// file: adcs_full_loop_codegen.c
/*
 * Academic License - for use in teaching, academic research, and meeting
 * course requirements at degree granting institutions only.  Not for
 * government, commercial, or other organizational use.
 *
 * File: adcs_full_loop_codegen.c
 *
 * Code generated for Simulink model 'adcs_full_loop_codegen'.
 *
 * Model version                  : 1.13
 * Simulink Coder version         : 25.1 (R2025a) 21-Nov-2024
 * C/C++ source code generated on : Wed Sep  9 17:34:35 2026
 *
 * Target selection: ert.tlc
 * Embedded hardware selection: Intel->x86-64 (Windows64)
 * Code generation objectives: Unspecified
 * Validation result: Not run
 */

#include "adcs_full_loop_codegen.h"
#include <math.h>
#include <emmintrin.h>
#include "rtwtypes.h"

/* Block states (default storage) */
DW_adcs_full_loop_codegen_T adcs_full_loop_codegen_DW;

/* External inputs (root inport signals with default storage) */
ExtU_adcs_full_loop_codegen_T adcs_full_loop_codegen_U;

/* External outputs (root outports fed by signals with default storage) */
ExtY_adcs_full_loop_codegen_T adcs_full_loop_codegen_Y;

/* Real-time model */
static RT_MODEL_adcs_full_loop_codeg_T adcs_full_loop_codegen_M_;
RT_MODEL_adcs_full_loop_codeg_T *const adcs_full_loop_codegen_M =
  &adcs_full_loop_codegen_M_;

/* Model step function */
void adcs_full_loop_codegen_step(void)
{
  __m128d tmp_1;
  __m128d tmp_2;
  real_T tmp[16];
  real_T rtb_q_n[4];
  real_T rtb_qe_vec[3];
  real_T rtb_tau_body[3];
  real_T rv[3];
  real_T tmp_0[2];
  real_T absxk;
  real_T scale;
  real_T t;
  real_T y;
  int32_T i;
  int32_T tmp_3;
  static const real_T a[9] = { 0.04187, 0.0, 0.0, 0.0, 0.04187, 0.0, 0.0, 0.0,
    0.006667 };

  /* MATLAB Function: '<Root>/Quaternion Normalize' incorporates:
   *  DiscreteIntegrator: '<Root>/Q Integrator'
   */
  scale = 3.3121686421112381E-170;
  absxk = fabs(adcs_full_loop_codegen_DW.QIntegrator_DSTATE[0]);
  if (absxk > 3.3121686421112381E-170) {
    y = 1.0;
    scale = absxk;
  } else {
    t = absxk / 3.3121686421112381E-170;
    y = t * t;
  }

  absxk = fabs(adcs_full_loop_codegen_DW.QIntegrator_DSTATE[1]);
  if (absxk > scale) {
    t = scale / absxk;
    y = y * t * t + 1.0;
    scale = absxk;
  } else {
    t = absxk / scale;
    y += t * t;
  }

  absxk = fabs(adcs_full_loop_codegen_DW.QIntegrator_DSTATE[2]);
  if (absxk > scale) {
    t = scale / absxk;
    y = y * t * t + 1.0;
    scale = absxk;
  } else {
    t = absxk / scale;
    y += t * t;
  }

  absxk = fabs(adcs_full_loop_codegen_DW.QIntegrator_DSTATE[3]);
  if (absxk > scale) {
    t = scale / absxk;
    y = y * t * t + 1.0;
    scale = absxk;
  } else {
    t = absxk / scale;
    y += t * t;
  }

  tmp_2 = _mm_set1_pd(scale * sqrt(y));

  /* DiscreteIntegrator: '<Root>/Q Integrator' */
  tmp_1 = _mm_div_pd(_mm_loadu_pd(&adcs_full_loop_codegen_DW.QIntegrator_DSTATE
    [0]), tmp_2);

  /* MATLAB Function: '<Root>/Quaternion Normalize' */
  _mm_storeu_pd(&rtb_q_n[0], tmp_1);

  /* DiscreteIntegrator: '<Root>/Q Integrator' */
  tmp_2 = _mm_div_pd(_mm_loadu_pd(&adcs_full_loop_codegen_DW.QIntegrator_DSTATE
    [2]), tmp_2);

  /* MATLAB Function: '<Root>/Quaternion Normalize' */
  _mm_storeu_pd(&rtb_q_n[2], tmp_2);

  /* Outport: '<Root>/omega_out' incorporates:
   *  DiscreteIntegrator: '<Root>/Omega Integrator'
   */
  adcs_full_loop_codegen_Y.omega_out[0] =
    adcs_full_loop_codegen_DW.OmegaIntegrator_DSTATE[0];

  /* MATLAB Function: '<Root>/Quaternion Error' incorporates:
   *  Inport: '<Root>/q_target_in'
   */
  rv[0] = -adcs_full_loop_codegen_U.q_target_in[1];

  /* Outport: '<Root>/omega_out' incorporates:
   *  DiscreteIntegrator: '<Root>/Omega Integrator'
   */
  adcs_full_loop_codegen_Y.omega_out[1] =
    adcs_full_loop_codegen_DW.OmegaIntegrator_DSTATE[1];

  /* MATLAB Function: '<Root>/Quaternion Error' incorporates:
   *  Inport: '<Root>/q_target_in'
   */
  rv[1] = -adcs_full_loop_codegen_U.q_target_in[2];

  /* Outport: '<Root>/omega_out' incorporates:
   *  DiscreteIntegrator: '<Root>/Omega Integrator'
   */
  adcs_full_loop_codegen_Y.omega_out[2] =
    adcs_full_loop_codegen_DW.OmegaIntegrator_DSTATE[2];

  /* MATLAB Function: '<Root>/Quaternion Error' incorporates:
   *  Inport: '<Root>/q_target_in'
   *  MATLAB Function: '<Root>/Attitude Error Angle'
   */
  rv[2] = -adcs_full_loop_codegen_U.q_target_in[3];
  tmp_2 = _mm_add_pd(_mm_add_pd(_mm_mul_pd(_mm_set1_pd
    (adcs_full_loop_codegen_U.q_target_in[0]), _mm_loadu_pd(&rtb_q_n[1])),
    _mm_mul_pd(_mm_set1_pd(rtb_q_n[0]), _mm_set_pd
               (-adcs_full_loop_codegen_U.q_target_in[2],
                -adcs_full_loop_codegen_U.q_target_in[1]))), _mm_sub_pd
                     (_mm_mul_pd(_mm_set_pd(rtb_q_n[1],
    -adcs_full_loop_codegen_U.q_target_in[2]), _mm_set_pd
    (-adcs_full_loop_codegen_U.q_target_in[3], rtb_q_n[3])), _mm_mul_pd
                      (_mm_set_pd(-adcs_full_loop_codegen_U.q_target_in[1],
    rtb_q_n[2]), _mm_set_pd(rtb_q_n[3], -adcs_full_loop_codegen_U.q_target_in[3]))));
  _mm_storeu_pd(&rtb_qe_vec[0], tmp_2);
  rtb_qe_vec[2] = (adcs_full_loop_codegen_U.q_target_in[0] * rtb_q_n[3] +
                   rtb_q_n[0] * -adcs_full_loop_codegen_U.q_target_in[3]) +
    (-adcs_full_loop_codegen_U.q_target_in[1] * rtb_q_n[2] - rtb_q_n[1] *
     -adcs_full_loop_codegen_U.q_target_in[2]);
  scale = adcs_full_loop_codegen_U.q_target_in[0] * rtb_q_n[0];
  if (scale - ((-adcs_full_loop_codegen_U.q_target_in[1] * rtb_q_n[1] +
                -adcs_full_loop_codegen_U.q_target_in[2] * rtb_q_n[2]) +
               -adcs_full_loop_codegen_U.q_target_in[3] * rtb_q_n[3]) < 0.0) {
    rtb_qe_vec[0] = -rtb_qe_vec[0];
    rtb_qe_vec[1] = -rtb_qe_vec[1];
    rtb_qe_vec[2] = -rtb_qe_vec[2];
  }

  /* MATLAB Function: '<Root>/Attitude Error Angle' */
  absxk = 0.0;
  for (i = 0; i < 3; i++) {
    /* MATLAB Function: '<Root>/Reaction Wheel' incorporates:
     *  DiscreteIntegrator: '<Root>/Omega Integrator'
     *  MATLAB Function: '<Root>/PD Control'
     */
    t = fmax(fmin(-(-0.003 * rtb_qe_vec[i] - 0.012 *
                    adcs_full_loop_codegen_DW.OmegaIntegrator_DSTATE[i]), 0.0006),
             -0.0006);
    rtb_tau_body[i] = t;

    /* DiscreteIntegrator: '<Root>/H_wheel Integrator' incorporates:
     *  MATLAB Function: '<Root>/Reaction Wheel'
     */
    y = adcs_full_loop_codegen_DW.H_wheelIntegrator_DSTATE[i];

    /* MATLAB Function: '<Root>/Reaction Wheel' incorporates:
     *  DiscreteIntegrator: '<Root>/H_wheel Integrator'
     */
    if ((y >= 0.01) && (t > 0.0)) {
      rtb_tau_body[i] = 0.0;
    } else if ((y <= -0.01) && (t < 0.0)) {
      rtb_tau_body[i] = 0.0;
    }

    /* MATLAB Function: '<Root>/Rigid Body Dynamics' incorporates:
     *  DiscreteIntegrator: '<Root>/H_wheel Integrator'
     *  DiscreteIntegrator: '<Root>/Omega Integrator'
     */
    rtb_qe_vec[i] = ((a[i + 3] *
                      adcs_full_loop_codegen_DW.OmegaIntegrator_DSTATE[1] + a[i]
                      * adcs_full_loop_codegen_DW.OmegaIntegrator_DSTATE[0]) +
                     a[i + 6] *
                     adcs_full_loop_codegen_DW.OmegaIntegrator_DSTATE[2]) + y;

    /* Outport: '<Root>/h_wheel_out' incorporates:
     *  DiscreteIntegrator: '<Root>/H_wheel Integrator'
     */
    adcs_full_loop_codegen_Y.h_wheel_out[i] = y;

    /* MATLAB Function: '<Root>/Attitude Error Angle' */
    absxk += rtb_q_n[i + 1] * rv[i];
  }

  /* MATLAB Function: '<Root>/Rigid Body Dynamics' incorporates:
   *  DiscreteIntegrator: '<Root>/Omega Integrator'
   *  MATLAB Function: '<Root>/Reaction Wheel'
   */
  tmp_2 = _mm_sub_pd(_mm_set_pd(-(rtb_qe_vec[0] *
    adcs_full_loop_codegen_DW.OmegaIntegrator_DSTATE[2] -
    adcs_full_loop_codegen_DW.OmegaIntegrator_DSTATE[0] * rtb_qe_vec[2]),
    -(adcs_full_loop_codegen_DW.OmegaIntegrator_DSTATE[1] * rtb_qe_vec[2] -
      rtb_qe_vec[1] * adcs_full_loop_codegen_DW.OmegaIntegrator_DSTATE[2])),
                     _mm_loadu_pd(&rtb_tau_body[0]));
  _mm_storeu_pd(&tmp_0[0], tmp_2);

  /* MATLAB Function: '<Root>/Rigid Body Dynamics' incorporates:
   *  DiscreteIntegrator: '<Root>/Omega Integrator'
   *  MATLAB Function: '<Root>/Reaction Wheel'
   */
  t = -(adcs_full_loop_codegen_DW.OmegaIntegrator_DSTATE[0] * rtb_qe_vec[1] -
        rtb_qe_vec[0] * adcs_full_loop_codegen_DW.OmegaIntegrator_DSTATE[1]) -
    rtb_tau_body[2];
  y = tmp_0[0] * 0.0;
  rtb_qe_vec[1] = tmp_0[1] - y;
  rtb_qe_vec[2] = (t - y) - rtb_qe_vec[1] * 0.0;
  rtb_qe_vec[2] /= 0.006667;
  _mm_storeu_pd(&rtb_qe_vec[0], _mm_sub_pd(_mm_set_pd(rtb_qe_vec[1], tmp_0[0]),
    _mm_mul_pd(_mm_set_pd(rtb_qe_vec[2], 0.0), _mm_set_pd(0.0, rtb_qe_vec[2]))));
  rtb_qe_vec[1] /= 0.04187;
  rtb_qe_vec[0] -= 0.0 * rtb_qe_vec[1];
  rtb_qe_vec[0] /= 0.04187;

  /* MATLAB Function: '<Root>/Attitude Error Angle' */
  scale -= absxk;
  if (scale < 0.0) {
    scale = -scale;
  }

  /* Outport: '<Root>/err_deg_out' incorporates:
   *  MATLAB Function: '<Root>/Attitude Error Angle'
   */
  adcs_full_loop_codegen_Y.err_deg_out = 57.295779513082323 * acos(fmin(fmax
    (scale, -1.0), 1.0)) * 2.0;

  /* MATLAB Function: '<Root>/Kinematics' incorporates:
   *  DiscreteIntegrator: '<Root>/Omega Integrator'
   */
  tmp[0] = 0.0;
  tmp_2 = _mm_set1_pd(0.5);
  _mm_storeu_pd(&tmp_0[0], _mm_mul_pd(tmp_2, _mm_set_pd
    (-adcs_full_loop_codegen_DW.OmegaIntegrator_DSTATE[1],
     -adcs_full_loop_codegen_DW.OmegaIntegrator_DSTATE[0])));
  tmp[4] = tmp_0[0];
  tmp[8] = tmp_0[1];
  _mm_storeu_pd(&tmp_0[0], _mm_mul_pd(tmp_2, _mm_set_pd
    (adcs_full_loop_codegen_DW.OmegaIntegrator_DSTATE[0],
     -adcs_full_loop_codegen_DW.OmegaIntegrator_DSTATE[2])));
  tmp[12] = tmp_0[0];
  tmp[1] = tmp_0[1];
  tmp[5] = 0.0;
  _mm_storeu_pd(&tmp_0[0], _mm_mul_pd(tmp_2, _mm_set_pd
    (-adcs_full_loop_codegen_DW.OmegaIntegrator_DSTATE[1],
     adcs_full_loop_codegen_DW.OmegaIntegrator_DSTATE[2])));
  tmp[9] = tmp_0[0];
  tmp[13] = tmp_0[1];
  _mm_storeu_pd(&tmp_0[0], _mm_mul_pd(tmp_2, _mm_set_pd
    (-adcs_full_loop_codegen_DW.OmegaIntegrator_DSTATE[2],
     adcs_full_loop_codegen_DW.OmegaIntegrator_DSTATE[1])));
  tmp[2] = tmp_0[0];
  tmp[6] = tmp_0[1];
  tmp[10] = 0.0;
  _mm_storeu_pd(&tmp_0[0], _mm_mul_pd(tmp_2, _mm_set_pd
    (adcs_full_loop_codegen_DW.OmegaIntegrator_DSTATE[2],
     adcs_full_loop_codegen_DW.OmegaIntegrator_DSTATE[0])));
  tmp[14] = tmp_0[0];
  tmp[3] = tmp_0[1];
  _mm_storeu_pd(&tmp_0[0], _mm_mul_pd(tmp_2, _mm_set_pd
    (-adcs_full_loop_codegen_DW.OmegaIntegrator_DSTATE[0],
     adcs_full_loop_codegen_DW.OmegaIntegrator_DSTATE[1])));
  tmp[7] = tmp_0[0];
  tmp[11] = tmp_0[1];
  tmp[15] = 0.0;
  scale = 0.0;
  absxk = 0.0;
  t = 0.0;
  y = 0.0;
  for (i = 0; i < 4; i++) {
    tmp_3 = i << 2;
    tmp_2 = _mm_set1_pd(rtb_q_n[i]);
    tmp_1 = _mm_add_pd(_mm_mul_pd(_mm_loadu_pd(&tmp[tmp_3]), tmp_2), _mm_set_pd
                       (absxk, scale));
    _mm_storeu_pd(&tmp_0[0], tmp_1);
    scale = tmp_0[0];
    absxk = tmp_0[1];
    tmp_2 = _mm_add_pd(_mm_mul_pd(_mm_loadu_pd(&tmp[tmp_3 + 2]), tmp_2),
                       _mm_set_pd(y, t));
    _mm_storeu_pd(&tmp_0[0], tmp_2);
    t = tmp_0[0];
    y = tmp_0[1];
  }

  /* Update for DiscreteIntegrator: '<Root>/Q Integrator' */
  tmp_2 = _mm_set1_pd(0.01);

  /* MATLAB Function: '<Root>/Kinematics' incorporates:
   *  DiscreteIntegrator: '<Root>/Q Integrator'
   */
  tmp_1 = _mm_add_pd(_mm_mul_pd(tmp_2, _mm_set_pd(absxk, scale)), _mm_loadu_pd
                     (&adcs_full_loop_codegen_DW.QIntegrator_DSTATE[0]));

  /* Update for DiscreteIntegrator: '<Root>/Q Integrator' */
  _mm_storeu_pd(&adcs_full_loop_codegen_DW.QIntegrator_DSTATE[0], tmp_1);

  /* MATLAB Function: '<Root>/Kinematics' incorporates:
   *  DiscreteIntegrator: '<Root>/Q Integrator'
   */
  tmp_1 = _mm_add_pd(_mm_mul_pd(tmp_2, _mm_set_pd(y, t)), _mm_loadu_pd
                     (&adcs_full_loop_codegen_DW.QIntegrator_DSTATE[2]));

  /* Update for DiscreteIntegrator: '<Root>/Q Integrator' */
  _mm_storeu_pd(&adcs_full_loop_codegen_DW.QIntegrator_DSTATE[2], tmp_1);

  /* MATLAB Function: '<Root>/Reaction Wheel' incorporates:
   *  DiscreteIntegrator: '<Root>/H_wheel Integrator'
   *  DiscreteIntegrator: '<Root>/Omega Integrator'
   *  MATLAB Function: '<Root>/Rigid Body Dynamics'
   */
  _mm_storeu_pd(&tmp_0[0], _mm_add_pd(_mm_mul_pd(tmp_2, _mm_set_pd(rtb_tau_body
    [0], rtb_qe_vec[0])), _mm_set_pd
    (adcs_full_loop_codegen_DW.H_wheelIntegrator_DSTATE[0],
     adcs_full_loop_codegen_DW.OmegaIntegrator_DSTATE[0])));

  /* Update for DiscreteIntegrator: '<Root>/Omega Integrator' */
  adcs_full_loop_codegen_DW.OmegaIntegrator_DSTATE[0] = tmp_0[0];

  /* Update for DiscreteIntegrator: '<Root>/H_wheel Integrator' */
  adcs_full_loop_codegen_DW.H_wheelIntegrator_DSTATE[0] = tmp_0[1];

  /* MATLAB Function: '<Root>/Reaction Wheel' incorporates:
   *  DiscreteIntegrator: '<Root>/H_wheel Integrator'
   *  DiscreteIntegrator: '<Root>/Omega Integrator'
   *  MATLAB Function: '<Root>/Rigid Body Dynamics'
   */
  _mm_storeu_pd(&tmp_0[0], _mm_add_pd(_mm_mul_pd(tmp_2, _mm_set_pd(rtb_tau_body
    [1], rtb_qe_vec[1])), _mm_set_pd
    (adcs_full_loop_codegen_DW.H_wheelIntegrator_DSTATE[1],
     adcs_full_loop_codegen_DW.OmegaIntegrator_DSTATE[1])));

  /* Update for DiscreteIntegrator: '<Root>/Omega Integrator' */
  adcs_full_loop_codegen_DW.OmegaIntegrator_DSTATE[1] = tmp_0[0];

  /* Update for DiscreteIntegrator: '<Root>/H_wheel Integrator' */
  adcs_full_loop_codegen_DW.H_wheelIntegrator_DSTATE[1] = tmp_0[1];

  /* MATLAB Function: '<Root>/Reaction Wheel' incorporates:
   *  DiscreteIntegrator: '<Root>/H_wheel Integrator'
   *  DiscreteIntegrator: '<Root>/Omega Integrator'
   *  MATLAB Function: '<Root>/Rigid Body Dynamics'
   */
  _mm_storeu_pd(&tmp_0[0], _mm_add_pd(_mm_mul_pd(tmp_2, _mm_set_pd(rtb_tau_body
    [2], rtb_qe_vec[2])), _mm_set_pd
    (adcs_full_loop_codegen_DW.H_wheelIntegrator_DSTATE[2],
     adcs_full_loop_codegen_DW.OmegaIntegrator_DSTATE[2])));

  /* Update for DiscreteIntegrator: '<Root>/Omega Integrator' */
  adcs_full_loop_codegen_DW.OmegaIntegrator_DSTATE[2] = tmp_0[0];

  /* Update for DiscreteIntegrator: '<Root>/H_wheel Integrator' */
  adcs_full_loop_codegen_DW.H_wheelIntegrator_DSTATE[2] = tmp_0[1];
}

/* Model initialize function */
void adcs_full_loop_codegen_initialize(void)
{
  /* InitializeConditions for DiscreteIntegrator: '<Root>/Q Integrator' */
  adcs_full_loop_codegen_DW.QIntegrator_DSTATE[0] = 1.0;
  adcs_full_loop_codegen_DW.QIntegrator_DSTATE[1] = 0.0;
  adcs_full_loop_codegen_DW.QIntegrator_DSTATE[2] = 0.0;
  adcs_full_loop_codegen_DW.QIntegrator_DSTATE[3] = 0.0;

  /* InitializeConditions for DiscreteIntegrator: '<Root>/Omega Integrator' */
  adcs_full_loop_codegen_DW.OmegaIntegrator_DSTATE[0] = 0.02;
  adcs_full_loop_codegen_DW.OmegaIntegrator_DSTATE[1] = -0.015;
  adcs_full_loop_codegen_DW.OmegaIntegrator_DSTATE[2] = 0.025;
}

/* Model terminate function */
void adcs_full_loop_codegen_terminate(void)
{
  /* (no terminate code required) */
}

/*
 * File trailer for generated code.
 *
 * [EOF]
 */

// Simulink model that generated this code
simulink model "adcs_full_loop_codegen"  (R2025a)
settings: Solver=ode4  StartTime=0.0  StopTime=800  FixedStep=0.01  RelTol=1e-8
undefined symbols (not defined in the file): DiscIntNeverNeededParam

== system adcs_full_loop_codegen ==
  q_target_in : Inport  PortDimensions=4
  Attitude Error Angle : MATLAB Function  TreatAsAtomicUnit=on
  Display : Display
  Display1 : Display
  Display2 : Display
  Error Scope : Scope
  H_wheel Integrator : DiscreteIntegrator  InitialCondition=[0;0;0]  SampleTime=0.01  ICPrevOutput=DiscIntNeverNeededParam  ICPrevScaledInput=DiscIntNeverNeededParam
  H_wheel Scope : Scope
  Kinematics : MATLAB Function  TreatAsAtomicUnit=on
  Omega Integrator : DiscreteIntegrator  InitialCondition=[0.02;-0.015;0.025]  SampleTime=0.01  ICPrevOutput=DiscIntNeverNeededParam  ICPrevScaledInput=DiscIntNeverNeededParam
  Omega Scope : Scope
  PD Control : MATLAB Function  TreatAsAtomicUnit=on
  Q Integrator : DiscreteIntegrator  InitialCondition=[1;0;0;0]  SampleTime=0.01  ICPrevOutput=DiscIntNeverNeededParam  ICPrevScaledInput=DiscIntNeverNeededParam
  Quaternion Error : MATLAB Function  TreatAsAtomicUnit=on
  Quaternion Normalize : MATLAB Function  TreatAsAtomicUnit=on
  Reaction Wheel : MATLAB Function  TreatAsAtomicUnit=on
  Rigid Body Dynamics : MATLAB Function  TreatAsAtomicUnit=on
  err_deg_out : Outport
  omega_out : Outport  Port=2
  h_wheel_out : Outport  Port=3
  wires:
  q_target_in/1 -> Attitude Error Angle/1(q_target), Quaternion Error/1(q_target)
  Quaternion Normalize/1(q_n) -> Attitude Error Angle/2(q), Quaternion Error/2(q), Kinematics/1(q)
  Q Integrator/1 -> Quaternion Normalize/1(q)
  Attitude Error Angle/1(err_deg) -> Error Scope/1, Display/1, err_deg_out/1
  PD Control/1(tau_cmd) -> Reaction Wheel/1(tau_cmd_body)
  Quaternion Error/1(qe_vec) -> PD Control/1(qe_vec)
  H_wheel Integrator/1 -> Reaction Wheel/2(h_wheel), Rigid Body Dynamics/2(h_wheel), h_wheel_out/1, H_wheel Scope/1, Display1/1
  Reaction Wheel/2(h_wheel_dot) -> H_wheel Integrator/1, Rigid Body Dynamics/3(h_wheel_dot)
  Omega Integrator/1 -> PD Control/2(omega), omega_out/1, Kinematics/2(omega), Rigid Body Dynamics/1(omega), Omega Scope/1, Display2/1
  Rigid Body Dynamics/1(omega_dot) -> Omega Integrator/1
  Kinematics/1(q_dot) -> Q Integrator/1

== matlab function adcs_full_loop_codegen/Kinematics ==
function q_dot = kinematics_block(q, omega)
    wx = omega(1); wy = omega(2); wz = omega(3);
    Omega = [ 0 -wx -wy -wz; wx 0 wz -wy; wy -wz 0 wx; wz wy -wx 0 ];
    q_dot = 0.5 * Omega * q;
end

== matlab function adcs_full_loop_codegen/Reaction Wheel ==
function [tau_body, h_wheel_dot] = reaction_wheel_block(tau_cmd_body, h_wheel)
    h_max = 0.01; tau_max = 0.0006;   % same values as reaction_wheel_model.m
    tau_wheel_cmd = -tau_cmd_body;     % same sign fix as the debugged .m version
    tau_actual = zeros(3,1);
    for i = 1:3
        tau_actual(i) = max(min(tau_wheel_cmd(i), tau_max), -tau_max);
    end
    for i = 1:3
        if (h_wheel(i) >= h_max && tau_actual(i) > 0) || ...
           (h_wheel(i) <= -h_max && tau_actual(i) < 0)
            tau_actual(i) = 0;
        end
    end
    h_wheel_dot = tau_actual;
    tau_body = -tau_actual;
end

== matlab function adcs_full_loop_codegen/Quaternion Normalize ==
function q_n = normalize_block(q)
    q_n = q / norm(q);
end

== matlab function adcs_full_loop_codegen/Attitude Error Angle ==
function err_deg = error_angle_block(q_target, q)
    q0 = q(1); qv = q(2:4);
    r0 = q_target(1); rv = -q_target(2:4);
    qe0 = r0*q0 - dot(rv,qv);
    if qe0 < 0, qe0 = -qe0; end
    qe0 = min(max(qe0,-1),1);
    err_deg = 2*acosd(qe0);
end

== matlab function adcs_full_loop_codegen/Quaternion Error ==
function qe_vec = quaternion_error_block(q_target, q)
    q0 = q(1); qv = q(2:4);
    r0 = q_target(1); rv = -q_target(2:4);  % conjugate of q_target inline
    qe0 = r0*q0 - dot(rv,qv);
    qe_vec = r0*qv + q0*rv + cross(rv,qv);
    if qe0 < 0
        qe_vec = -qe_vec;   % shortest-path correction, same as pid_attitude_control.m
    end
end

== matlab function adcs_full_loop_codegen/PD Control ==
function tau_cmd = pd_control_block(qe_vec, omega)
    Kp = 3e-3;   % SAME gains as main_pointing.m -- keep in sync if you retune
    Kd = 1.2e-2;
    tau_cmd = -Kp*qe_vec - Kd*omega;
end

== matlab function adcs_full_loop_codegen/Rigid Body Dynamics ==
function omega_dot = rigid_body_dynamics_block(omega, h_wheel, h_wheel_dot)
    I = diag([0.04187, 0.04187, 0.006667]);   % same 3U CubeSat inertia as inertia_properties.m
    H_total = I*omega + h_wheel;
    gyroscopic_term = cross(omega, H_total);
    omega_dot = I \ (-gyroscopic_term - h_wheel_dot);   % tau_ext = 0 (pointing loop only, no disturbance)
end
